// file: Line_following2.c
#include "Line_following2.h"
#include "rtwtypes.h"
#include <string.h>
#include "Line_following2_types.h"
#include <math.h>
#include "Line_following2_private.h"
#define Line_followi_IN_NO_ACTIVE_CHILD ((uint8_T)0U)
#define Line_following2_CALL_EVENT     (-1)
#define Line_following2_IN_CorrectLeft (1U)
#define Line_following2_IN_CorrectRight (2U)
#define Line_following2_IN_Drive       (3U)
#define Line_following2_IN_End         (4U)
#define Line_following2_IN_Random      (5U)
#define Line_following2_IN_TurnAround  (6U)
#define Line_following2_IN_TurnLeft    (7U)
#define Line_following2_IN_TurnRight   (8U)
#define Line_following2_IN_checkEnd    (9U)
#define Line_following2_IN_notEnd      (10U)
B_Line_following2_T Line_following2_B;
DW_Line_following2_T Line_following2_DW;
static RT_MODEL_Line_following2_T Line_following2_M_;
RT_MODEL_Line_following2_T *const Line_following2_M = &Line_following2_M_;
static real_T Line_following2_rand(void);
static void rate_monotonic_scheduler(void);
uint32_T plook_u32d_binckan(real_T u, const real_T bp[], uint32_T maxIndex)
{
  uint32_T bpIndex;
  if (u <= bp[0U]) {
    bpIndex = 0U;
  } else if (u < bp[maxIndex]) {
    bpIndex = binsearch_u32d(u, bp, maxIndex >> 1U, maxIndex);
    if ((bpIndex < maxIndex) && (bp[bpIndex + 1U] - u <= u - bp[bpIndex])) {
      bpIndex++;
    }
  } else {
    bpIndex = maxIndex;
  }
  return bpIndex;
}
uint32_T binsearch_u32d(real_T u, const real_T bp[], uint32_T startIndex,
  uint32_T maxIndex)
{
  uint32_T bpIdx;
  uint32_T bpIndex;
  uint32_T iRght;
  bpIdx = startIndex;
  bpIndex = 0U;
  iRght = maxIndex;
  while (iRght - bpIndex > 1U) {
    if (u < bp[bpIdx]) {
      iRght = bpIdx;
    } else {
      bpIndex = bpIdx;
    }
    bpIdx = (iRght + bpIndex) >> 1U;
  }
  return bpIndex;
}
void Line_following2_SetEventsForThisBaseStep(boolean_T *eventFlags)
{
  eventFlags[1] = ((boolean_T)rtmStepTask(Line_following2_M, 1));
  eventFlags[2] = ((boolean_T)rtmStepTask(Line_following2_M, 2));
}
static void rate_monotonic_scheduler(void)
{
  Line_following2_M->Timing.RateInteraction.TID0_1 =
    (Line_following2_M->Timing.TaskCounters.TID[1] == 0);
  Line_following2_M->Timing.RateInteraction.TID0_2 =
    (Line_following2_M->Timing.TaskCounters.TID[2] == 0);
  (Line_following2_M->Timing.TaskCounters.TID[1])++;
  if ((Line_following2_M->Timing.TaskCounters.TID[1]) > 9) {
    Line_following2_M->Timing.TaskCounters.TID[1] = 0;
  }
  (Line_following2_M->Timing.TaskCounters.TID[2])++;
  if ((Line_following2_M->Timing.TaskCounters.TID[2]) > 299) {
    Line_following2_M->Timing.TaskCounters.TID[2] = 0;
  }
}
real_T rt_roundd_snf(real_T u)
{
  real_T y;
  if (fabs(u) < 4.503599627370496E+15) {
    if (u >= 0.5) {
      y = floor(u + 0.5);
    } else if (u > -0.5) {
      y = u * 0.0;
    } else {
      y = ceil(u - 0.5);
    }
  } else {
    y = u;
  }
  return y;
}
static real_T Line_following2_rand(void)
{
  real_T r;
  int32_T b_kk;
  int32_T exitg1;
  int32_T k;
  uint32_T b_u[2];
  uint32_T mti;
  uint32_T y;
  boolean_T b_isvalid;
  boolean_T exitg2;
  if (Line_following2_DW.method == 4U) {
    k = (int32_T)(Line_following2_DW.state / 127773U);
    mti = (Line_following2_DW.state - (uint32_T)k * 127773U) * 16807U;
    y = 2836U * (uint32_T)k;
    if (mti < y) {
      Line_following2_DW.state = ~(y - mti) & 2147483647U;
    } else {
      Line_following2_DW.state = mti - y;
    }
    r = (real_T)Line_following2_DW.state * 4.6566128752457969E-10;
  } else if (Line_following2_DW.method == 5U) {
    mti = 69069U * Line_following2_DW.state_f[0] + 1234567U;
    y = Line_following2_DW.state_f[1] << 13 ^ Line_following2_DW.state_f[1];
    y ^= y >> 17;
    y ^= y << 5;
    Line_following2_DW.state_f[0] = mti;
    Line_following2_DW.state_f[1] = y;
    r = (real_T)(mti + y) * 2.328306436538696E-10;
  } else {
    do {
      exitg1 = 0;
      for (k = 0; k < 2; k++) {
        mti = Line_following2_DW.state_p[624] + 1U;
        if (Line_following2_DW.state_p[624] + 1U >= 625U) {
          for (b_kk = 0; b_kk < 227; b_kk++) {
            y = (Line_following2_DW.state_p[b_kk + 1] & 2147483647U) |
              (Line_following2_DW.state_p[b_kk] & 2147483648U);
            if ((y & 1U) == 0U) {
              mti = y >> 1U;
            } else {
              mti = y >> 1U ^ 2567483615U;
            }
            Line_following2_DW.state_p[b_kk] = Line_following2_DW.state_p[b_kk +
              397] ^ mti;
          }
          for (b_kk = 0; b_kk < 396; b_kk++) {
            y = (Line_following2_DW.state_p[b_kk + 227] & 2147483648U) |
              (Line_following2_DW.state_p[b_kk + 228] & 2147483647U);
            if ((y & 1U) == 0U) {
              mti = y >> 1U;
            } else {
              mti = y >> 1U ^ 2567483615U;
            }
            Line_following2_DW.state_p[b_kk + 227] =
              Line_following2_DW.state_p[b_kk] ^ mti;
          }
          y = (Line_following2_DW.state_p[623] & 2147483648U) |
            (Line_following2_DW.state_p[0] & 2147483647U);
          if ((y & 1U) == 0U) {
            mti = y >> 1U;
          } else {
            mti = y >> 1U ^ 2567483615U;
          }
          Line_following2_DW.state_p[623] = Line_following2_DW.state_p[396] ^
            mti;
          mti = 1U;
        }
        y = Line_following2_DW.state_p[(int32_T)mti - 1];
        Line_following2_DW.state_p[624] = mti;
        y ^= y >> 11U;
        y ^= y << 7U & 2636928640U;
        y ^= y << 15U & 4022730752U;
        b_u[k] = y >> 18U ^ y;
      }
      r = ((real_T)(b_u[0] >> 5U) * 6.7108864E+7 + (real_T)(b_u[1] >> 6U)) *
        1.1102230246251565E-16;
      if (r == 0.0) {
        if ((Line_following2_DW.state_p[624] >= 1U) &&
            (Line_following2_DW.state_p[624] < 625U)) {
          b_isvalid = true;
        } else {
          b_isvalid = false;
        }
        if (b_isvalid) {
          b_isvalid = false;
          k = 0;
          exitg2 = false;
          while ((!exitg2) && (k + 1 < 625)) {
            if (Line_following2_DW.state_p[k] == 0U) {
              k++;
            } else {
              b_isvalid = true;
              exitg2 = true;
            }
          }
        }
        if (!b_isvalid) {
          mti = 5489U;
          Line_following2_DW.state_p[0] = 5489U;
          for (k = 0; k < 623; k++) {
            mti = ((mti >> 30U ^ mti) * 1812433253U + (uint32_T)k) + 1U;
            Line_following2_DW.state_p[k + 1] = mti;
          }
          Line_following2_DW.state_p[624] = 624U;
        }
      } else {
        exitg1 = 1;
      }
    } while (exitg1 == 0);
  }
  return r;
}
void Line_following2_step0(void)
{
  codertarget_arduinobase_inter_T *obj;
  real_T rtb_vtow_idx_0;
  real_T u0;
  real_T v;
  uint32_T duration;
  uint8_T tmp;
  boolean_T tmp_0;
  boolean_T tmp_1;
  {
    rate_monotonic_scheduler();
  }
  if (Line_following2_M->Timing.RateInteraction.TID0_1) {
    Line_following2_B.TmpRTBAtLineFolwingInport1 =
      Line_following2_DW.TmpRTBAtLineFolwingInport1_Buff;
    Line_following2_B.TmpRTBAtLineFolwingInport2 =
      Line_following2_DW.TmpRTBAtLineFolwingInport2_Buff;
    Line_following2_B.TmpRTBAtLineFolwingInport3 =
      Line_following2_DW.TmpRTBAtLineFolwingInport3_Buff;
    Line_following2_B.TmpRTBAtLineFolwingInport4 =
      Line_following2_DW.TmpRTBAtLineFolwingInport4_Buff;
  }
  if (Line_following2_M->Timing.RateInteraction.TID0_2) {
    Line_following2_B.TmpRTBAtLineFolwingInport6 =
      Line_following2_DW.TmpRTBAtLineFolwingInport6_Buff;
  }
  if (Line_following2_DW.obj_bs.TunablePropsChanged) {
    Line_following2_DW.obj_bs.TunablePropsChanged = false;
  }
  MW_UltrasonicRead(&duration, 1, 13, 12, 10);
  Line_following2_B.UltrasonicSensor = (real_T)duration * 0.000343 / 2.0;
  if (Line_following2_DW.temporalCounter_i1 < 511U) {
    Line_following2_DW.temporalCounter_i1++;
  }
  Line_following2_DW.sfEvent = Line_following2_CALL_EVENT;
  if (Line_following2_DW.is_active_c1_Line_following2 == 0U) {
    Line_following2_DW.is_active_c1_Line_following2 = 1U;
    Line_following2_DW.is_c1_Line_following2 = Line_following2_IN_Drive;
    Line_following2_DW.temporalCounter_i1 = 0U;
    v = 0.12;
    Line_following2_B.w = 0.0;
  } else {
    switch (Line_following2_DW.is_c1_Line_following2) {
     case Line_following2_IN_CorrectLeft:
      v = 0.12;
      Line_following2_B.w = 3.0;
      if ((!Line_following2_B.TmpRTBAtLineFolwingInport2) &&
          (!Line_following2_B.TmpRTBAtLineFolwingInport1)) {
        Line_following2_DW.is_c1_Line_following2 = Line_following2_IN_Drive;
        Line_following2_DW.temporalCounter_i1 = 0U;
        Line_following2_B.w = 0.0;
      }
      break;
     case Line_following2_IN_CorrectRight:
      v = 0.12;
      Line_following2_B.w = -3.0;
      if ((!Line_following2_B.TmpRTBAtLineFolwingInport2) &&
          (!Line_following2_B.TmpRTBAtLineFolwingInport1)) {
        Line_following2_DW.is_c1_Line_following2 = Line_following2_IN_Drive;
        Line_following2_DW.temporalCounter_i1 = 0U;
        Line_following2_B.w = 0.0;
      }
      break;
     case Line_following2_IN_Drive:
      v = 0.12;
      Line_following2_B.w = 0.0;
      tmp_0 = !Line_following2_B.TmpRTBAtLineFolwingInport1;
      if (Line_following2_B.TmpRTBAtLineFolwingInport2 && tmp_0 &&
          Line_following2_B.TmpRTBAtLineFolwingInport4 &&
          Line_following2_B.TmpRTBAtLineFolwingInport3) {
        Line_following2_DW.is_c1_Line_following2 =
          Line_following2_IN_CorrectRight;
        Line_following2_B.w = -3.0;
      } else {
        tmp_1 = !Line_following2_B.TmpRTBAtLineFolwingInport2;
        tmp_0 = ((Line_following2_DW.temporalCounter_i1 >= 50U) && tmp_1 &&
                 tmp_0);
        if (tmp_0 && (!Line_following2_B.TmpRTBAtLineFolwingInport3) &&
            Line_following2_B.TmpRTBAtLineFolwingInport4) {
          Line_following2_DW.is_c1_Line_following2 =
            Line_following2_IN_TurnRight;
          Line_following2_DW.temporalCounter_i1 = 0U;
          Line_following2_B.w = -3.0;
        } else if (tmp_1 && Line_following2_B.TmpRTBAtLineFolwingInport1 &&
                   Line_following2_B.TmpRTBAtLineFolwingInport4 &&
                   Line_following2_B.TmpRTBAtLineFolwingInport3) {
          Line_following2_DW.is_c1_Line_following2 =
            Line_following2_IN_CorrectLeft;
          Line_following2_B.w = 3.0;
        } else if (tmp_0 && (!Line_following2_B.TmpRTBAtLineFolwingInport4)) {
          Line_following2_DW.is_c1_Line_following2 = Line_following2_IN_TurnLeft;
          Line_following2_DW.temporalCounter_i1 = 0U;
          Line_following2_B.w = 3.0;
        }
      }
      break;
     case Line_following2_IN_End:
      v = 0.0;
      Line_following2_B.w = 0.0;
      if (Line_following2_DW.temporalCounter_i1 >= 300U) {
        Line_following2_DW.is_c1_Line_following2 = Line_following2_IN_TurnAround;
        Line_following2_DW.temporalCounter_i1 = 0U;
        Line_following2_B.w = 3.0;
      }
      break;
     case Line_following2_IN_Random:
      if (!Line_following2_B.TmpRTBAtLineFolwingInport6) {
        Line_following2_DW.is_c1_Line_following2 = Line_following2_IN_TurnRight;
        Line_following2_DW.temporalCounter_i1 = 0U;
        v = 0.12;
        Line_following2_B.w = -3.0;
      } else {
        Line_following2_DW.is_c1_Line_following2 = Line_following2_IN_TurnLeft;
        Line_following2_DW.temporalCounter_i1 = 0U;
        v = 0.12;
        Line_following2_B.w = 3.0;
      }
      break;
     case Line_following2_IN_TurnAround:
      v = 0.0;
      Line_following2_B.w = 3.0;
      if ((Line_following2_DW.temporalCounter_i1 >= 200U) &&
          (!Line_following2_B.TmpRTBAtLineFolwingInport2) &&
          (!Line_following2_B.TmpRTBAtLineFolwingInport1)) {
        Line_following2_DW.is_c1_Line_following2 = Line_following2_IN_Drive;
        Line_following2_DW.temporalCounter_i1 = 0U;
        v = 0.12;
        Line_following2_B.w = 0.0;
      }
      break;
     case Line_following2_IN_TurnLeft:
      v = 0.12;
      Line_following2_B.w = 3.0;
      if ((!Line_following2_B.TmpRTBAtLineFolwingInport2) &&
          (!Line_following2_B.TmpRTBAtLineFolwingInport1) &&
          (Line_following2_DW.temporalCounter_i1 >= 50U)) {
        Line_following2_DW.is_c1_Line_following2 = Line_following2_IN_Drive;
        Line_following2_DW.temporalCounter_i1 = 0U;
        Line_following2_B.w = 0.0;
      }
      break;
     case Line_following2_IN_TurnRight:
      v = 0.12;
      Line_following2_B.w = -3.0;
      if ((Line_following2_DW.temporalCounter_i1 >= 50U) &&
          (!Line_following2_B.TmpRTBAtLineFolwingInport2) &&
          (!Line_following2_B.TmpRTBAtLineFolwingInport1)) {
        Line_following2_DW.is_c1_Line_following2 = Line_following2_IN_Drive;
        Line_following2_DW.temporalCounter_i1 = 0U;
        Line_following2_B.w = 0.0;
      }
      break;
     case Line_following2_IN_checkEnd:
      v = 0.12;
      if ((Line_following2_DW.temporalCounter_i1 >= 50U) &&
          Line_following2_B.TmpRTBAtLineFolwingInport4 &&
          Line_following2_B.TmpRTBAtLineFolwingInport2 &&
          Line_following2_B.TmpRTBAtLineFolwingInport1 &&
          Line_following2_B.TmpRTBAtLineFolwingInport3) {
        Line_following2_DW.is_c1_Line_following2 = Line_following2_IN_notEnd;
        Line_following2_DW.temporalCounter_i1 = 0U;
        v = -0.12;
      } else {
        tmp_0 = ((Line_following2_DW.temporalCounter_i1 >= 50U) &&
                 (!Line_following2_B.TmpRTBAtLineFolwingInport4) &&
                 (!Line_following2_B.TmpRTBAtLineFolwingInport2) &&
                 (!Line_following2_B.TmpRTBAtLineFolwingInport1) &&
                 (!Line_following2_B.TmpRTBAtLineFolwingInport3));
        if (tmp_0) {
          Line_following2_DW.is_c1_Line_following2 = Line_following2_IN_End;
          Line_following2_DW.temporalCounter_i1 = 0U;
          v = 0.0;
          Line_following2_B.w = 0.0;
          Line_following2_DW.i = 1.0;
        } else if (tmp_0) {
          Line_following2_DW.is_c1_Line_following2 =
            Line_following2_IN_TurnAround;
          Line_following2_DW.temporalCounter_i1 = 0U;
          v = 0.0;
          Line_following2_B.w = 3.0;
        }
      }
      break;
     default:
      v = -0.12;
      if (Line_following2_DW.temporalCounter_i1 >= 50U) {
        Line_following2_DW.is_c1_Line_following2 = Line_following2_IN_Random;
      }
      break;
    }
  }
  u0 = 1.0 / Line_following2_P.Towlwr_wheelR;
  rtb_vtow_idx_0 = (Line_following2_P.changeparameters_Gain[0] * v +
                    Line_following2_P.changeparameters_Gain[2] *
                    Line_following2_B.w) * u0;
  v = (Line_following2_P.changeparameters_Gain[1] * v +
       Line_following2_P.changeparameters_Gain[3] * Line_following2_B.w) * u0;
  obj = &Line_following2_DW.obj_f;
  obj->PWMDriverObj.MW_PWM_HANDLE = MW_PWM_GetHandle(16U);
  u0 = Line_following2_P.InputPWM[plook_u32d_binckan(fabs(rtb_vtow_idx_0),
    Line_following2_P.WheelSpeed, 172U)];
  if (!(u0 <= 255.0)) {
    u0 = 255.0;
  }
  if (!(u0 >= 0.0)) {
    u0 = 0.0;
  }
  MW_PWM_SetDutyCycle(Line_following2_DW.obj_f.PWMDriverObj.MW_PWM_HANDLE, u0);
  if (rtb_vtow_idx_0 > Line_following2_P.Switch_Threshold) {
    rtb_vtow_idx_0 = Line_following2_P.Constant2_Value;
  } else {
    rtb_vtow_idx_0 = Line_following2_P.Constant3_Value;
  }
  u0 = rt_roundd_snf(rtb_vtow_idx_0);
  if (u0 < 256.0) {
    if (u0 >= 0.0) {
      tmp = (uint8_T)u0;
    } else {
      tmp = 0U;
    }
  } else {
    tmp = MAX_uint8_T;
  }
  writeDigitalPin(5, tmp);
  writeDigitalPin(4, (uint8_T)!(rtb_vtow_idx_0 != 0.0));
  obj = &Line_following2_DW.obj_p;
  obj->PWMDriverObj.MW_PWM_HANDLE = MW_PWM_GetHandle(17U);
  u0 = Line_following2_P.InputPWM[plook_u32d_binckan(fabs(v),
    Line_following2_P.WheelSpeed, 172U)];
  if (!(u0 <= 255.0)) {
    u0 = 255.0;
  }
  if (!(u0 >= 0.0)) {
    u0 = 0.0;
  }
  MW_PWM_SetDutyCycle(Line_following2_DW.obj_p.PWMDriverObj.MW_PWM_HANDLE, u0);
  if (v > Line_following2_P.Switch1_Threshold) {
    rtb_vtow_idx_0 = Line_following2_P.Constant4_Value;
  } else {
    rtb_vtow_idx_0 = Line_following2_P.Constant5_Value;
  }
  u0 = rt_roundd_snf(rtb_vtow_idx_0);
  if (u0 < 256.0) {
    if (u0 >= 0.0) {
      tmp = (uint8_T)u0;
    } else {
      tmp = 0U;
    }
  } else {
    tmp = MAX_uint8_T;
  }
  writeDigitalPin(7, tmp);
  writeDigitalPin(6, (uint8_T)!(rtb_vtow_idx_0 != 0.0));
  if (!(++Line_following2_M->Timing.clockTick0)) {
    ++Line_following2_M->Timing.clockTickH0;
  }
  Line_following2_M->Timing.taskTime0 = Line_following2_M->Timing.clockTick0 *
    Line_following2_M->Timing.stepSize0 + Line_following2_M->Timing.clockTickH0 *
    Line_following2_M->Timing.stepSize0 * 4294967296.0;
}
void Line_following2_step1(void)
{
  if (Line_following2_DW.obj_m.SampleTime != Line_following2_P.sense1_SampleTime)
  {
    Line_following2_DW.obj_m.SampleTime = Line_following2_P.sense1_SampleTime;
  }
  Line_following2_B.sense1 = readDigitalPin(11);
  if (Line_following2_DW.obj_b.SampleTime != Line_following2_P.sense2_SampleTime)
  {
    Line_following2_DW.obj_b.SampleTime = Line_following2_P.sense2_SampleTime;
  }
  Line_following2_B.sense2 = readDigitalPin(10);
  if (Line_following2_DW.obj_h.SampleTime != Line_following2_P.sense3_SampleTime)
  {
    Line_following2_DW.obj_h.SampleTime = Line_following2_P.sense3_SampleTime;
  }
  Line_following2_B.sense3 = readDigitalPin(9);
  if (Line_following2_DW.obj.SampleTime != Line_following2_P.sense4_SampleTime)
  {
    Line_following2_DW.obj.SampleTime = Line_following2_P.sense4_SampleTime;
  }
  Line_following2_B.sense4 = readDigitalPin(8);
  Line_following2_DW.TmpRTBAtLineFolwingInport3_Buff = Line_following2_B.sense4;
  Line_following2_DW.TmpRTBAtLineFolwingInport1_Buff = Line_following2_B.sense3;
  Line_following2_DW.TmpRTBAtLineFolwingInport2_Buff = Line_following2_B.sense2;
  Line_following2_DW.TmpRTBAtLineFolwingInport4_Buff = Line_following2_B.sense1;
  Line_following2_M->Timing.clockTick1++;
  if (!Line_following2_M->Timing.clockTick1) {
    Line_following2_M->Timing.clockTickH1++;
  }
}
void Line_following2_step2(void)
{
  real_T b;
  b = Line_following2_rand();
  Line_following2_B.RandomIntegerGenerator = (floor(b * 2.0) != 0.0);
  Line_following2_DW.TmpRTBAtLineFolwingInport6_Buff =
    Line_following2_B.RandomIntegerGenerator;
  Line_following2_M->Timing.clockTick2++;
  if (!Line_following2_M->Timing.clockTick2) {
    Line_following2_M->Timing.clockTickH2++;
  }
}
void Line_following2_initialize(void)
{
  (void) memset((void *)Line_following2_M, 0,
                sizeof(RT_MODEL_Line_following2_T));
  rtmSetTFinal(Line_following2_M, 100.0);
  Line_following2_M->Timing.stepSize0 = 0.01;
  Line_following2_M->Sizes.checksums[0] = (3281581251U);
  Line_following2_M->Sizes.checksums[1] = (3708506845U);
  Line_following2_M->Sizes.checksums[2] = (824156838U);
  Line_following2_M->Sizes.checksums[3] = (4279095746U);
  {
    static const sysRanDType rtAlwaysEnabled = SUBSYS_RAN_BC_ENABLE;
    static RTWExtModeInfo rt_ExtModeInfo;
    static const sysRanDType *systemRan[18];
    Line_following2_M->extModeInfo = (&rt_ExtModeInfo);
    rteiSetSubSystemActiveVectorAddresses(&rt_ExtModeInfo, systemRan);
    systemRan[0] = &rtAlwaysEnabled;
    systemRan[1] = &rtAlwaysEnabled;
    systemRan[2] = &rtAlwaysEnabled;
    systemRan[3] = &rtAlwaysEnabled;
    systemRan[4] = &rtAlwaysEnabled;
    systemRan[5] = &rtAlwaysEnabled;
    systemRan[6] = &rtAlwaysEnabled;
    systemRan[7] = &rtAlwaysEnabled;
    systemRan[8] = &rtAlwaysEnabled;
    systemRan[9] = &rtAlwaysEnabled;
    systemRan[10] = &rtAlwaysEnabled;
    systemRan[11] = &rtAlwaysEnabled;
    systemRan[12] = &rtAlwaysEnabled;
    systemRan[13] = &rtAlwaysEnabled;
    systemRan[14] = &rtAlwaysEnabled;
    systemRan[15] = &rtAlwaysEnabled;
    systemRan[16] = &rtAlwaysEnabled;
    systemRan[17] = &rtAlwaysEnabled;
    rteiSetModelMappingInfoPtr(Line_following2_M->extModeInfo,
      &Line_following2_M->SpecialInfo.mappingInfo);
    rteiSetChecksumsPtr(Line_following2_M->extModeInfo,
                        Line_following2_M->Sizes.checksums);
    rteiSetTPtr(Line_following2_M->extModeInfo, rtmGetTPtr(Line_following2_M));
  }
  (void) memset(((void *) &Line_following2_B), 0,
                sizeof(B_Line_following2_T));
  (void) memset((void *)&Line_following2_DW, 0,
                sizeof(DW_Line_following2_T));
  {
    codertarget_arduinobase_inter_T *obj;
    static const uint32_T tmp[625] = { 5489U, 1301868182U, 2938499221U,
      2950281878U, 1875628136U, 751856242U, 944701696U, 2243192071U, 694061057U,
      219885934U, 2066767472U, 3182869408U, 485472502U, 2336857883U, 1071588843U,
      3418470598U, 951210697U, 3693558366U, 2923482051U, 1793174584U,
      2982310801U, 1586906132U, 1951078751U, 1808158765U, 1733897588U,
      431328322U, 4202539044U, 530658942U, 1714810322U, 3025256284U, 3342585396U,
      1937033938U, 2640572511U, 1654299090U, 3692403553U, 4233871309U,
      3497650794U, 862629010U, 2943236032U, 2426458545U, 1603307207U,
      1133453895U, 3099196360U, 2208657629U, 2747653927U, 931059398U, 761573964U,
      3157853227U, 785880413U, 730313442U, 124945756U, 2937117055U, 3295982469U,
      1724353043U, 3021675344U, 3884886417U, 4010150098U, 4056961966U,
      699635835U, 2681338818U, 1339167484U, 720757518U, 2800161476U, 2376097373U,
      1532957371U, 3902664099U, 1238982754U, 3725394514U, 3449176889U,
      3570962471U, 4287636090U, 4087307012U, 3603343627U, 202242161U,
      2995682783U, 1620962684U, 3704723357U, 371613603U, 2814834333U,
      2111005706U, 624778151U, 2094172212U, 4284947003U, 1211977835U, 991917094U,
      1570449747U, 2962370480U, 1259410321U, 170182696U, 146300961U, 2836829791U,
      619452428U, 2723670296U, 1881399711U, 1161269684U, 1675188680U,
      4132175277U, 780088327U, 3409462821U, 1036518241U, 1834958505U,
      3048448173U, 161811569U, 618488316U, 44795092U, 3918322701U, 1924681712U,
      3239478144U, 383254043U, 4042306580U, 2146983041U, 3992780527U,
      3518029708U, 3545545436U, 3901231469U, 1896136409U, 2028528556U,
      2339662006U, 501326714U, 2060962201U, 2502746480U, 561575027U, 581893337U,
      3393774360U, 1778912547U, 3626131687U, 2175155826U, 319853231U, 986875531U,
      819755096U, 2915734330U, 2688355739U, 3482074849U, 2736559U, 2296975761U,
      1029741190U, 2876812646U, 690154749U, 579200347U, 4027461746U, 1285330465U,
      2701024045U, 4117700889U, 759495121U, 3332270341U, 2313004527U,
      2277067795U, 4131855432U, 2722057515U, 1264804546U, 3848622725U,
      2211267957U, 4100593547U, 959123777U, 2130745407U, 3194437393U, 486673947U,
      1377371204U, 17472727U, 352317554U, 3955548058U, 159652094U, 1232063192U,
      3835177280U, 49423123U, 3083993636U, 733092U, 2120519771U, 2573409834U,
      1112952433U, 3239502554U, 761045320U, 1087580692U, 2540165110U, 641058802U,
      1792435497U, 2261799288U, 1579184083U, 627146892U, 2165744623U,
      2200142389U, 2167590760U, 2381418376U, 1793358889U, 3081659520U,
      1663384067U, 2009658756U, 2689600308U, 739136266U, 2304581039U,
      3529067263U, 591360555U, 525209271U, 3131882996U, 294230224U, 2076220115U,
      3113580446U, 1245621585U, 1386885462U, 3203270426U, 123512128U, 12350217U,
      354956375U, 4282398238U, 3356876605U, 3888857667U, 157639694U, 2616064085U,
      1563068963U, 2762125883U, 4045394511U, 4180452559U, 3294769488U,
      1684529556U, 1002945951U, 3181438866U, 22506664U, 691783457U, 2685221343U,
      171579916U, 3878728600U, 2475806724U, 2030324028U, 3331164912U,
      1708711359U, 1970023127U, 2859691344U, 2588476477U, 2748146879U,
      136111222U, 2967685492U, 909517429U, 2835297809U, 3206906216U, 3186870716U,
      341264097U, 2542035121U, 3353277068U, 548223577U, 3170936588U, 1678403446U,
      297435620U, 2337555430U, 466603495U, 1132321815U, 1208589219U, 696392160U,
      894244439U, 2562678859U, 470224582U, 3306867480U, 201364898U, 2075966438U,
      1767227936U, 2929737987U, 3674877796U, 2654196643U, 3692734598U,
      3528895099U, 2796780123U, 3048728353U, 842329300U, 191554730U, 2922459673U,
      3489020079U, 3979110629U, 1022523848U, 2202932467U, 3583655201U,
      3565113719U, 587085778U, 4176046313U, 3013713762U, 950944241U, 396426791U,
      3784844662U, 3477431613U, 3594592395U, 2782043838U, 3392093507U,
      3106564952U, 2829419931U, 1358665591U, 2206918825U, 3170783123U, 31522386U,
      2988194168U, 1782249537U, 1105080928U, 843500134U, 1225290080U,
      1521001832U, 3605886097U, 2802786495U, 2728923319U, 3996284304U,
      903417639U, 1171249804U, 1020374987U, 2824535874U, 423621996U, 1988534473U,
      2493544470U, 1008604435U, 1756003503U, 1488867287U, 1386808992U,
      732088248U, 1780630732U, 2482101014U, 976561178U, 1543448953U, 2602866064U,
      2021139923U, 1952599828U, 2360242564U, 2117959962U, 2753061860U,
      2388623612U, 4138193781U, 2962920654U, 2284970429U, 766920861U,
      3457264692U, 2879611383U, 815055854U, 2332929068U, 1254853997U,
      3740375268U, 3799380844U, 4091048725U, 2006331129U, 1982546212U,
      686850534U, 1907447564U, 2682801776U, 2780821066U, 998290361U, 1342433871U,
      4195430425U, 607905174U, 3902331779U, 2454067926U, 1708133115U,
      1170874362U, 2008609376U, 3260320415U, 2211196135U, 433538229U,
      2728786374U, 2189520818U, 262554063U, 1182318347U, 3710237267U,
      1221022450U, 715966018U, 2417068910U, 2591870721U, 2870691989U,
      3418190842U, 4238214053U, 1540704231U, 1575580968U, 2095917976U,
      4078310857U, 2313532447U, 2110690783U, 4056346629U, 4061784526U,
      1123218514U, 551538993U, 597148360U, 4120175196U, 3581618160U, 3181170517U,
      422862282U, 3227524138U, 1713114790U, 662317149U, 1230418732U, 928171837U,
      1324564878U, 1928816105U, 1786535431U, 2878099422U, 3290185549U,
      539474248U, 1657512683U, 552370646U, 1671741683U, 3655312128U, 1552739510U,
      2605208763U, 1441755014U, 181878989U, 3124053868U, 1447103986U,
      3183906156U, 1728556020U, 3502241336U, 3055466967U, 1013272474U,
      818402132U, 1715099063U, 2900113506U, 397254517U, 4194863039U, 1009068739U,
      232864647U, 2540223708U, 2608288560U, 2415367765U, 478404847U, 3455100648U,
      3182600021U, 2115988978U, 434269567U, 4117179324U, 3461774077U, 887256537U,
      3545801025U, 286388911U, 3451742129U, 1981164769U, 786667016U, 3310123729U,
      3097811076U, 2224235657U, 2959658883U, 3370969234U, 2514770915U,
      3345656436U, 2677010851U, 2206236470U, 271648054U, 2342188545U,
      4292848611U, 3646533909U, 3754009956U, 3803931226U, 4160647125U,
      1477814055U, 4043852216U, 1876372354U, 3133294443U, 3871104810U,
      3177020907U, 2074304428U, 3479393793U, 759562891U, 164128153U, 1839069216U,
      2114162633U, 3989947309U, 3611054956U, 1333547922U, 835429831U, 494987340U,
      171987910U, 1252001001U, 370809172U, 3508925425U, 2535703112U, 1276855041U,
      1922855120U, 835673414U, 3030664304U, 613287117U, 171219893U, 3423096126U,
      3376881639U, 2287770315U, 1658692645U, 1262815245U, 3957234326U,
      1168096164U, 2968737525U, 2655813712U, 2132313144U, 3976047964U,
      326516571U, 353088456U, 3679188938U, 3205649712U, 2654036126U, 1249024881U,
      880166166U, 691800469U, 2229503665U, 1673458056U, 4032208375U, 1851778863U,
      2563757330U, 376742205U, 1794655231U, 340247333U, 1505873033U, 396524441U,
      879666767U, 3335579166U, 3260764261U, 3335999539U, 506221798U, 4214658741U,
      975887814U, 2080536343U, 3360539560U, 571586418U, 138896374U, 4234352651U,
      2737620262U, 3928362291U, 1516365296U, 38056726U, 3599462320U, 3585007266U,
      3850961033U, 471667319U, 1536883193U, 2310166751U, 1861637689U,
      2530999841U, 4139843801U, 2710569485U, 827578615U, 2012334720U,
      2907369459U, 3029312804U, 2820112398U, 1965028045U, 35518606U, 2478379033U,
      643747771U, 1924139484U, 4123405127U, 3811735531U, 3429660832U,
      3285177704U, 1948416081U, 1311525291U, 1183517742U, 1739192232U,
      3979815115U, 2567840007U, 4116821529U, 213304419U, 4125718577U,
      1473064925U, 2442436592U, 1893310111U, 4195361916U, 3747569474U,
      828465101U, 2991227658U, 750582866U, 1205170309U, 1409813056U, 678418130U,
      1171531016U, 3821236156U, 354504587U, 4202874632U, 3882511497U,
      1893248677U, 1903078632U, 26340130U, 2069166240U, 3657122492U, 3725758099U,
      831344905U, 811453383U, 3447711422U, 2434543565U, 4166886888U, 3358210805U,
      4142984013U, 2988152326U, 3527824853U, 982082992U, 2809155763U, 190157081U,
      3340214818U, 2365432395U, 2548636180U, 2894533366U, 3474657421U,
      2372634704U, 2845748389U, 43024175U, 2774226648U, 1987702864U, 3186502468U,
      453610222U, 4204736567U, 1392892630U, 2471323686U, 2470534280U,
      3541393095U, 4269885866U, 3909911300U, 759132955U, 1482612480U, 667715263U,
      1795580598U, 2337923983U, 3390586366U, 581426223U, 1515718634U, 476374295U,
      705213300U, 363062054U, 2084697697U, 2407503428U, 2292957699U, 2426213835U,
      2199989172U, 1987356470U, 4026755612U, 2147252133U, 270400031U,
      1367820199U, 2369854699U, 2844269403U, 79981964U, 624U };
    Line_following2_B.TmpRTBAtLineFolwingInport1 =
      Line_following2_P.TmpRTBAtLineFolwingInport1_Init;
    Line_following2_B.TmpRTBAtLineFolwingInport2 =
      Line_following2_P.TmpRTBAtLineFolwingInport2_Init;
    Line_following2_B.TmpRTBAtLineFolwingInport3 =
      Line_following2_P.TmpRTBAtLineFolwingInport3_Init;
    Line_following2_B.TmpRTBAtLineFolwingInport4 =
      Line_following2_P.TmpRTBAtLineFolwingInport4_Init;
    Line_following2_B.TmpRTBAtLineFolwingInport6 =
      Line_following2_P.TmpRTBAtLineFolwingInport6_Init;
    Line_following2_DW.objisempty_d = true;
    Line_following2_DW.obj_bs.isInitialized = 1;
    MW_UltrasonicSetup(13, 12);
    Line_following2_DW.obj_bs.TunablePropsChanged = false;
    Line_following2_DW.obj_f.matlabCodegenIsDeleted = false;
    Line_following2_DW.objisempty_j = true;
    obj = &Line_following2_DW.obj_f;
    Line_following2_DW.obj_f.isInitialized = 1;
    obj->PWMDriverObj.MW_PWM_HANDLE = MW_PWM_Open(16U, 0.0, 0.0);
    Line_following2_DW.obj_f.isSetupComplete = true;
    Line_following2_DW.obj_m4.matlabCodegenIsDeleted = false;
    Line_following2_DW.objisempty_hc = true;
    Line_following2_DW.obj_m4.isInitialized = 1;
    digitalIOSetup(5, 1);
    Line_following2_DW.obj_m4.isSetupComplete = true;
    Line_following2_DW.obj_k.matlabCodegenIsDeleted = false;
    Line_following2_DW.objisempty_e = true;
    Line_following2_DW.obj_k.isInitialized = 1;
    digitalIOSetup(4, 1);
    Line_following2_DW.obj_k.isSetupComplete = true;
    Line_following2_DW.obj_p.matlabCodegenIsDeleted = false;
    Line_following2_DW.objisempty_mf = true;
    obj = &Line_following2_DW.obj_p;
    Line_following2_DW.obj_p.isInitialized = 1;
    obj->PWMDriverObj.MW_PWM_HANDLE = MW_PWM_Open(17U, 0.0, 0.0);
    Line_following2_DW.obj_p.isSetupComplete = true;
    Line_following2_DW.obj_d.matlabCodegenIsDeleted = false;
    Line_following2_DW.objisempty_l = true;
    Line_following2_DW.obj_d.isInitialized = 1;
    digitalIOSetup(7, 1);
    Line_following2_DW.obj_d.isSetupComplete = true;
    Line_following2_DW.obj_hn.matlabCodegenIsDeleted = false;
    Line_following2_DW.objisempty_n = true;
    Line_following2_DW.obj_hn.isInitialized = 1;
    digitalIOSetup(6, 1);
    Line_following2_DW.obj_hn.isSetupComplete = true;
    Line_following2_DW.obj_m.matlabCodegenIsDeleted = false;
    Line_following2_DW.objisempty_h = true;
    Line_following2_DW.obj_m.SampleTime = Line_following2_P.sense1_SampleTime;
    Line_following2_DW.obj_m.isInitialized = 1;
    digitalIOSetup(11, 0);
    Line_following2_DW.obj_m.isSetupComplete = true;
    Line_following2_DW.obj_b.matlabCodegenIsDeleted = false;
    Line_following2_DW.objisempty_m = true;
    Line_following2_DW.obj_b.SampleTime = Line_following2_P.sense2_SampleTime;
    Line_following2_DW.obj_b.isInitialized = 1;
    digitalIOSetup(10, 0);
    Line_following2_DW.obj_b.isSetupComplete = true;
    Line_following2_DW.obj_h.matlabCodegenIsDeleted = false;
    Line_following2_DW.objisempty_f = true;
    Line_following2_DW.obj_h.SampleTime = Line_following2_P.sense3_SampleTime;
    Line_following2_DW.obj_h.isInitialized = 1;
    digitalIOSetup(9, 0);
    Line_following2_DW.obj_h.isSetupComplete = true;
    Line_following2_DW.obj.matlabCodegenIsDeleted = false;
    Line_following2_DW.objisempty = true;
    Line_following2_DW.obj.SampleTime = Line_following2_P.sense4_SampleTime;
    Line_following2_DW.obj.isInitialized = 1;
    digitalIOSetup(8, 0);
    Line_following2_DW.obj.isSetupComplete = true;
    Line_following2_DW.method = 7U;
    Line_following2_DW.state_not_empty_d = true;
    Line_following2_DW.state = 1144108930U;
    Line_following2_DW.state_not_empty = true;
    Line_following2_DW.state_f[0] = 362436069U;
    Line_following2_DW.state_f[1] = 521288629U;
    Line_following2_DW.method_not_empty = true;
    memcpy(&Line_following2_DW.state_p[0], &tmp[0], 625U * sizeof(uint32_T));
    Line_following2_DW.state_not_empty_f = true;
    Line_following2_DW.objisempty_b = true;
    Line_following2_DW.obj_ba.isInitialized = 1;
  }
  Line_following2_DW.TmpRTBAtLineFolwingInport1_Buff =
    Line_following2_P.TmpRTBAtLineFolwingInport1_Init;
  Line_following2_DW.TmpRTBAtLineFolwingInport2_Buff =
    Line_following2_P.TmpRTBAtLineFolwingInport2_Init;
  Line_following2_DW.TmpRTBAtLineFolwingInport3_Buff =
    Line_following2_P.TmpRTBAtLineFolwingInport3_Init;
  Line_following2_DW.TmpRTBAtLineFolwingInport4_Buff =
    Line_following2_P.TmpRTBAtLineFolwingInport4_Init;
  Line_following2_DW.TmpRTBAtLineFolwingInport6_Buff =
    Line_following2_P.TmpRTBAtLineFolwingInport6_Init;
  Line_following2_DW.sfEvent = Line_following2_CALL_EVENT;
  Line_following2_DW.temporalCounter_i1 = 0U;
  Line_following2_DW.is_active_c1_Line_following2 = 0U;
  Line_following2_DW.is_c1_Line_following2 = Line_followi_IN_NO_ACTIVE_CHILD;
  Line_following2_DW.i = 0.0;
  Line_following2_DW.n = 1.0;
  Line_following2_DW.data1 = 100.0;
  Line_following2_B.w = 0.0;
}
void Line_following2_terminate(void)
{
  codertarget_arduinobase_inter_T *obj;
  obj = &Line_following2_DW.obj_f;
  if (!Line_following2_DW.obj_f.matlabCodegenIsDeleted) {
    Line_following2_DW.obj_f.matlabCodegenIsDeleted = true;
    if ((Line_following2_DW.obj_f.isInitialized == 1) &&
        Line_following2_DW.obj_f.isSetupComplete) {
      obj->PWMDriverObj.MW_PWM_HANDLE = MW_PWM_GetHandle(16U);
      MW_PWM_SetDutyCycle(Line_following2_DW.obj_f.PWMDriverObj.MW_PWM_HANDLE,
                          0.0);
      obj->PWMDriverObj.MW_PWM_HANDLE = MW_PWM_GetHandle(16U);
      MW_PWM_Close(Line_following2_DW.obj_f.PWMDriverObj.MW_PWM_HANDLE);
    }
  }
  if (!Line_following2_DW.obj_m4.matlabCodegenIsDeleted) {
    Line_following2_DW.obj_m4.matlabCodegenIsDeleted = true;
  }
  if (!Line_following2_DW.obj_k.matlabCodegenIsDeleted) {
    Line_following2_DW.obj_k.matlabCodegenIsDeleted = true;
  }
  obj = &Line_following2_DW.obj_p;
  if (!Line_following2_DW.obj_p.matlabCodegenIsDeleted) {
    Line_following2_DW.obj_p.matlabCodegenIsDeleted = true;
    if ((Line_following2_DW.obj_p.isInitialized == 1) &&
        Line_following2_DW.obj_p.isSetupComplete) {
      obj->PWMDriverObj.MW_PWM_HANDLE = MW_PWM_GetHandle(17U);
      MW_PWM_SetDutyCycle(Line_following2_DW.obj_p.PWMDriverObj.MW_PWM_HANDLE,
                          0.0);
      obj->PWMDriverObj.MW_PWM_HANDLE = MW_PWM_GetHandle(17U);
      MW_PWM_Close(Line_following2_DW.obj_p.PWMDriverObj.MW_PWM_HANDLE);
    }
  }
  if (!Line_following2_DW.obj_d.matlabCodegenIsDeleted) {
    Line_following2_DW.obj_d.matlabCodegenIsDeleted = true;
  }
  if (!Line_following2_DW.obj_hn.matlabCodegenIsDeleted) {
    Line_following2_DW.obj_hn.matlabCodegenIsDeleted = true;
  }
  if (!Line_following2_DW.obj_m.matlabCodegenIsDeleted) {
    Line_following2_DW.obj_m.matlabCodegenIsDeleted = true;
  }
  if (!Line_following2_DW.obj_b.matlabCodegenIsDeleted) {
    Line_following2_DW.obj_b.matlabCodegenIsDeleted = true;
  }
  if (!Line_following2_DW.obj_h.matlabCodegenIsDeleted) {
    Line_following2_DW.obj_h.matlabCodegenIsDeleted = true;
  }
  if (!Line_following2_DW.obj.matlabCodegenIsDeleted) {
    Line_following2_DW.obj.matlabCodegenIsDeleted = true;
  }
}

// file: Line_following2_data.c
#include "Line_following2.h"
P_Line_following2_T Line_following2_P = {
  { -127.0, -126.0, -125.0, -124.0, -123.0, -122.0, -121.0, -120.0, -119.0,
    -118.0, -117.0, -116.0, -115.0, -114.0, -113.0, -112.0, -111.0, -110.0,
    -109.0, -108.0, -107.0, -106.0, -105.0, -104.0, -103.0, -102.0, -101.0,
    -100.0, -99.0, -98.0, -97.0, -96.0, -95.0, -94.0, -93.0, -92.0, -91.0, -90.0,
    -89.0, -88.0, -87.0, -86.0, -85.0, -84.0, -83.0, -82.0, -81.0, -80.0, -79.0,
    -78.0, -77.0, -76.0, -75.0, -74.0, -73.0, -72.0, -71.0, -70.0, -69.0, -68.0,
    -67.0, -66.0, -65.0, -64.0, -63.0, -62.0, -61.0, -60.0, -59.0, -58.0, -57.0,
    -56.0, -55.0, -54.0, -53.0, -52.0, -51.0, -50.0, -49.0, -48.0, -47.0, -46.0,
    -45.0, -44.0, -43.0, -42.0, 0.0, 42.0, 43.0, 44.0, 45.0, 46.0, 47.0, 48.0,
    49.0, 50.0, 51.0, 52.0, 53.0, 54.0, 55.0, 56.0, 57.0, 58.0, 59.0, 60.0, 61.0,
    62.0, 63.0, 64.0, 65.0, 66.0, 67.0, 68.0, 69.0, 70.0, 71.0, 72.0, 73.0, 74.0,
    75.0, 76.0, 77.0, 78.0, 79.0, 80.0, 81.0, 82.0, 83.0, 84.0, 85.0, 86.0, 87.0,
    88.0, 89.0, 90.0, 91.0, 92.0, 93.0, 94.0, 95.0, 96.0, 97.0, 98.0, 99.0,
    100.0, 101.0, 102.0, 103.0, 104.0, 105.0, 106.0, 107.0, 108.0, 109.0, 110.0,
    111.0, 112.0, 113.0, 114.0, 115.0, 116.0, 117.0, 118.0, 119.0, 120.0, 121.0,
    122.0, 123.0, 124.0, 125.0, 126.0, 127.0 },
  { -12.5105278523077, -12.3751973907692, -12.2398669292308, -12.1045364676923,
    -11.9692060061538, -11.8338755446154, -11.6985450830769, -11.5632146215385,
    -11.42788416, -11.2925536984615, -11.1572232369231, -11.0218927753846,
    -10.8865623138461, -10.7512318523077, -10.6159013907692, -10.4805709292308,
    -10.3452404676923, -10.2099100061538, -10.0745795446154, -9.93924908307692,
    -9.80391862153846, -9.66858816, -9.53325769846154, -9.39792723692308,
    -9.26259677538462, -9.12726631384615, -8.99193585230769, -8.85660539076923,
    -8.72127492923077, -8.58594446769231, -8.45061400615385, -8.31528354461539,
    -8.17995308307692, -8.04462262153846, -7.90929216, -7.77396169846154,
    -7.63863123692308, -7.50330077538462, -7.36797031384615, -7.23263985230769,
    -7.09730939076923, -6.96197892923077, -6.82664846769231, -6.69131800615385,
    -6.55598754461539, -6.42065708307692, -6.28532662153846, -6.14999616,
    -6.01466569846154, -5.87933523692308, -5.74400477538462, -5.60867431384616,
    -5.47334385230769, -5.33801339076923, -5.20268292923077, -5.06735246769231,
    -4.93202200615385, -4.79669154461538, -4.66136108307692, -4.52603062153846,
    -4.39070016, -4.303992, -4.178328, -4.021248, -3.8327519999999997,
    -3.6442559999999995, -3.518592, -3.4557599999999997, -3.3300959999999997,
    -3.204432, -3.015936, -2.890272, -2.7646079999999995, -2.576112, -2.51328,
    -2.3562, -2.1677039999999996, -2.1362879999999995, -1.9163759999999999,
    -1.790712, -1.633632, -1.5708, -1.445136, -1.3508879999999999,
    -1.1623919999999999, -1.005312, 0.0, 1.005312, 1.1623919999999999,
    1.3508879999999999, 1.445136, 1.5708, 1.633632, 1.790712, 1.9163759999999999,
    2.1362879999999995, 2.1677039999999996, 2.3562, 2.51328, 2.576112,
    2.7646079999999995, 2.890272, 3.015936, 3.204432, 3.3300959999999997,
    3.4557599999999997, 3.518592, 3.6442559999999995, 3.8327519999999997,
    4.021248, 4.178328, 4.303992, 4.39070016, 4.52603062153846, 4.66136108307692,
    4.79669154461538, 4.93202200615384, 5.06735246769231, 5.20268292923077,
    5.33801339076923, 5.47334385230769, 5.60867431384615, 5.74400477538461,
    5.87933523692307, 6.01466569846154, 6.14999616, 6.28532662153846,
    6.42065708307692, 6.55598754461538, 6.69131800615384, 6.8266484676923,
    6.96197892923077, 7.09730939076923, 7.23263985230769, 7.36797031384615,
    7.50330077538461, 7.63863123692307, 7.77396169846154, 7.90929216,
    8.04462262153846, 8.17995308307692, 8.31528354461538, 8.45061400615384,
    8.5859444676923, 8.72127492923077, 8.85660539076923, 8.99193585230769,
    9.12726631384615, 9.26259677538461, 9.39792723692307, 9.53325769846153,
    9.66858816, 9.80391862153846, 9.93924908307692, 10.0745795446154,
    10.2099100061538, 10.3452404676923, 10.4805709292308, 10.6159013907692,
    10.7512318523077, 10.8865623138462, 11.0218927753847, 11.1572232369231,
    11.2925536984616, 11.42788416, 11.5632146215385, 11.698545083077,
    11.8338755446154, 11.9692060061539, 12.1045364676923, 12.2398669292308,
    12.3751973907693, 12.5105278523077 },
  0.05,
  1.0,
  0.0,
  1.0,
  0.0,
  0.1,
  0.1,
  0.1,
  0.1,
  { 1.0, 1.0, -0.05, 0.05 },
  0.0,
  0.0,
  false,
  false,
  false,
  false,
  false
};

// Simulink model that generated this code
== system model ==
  PWM#1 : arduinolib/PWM  pinNumber=16  <- 1: Lookup_nD#1
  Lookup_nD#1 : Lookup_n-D  BreakpointsForDimension1=WheelSpeed  Table=InputPWM  InterpMethod=Nearest  <- 1: Abs#1
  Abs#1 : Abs  <- 1: Towlwr
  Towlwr : mobileRoboticsTrainingLib/To wlwr  <- 1: Stateflowchart#1, 2: Stateflowchart#1/2
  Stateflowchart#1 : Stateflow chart  <- 1: sense3, 2: sense2, 3: sense4, 4: sense1, 5: UltrasonicSensor, 6: RandomIntegerGenerator
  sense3 : arduinolib/Digital Input  pinNumber=9
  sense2 : arduinolib/Digital Input  pinNumber=10
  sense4 : arduinolib/Digital Input  pinNumber=8
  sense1 : arduinolib/Digital Input  pinNumber=11
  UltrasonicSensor : arduinosensorlib/Ultrasonic Sensor
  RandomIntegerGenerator : commrandsrc3/Random Integer Generator
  DigitalOutput#1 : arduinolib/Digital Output  pinNumber=5  <- 1: Switch
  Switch : Switch  Criteria=u2 > Threshold  <- 1: Constant2, 2: Towlwr, 3: Constant3
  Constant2 : Constant
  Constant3 : Constant  Value=0
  DigitalOutput#2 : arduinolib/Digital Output  pinNumber=4  <- 1: Logic#1
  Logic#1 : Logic  Operator=NOT  <- 1: Switch
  PWM#2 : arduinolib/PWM  pinNumber=17  <- 1: Lookup_nD#2
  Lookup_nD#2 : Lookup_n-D  BreakpointsForDimension1=WheelSpeed  Table=InputPWM  InterpMethod=Nearest  <- 1: Abs#2
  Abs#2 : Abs  <- 1: Towlwr/2
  DigitalOutput#3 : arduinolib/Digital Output  pinNumber=7  <- 1: Switch1
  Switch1 : Switch  Criteria=u2 > Threshold  <- 1: Constant4, 2: Towlwr/2, 3: Constant5
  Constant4 : Constant
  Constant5 : Constant  Value=0
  DigitalOutput#4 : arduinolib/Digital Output  pinNumber=6  <- 1: Logic#2
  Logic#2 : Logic  Operator=NOT  <- 1: Switch1
== stateflow chart Stateflowchart#1 ==
  state Random
    entry:
    dir;
  state notEnd
    entry:
    v=-0.12;
  state End
    entry:
    v=0;
    w=0;
    i=1;
  state TurnAround
    entry:
    v=0;
    w=3;
  state checkEnd
    entry:
    v=0.12;
  state TurnLeft
    entry:
    v=0.12;
    w=3;
  state TurnRight
    entry:
    v=0.12;
    w=-3;
  state Drive
    entry:
    v=0.12;
    w=0;
    i;
    n;
    data1;
  state CorrectLeft
    entry:
    v=0.12;
    w=3
  state CorrectRight
    entry:
    v=0.12;
    w=-3
  state ObjectDetected
    entry:
    v=0.12;
  state CorrectRight1
    entry:
    w=-3;
  state CorrectLeft1
    entry:
    w=3;
  state TurnAround1
    entry:
    w=3;
  state EndOfLine
    entry:
    v=0;
  state update
    entry:
    data1=ultraSonic;
  state WeOUT
    entry:
    v=0;
    w=0;
  checkEnd -> TurnAround [order 3] : [after(0.5,sec) &&sense1 ==0 && sense2 == 0 && sense3 ==0 && sense4==0 && i==1]
  Random -> TurnLeft [order 2] : [dir==1]
  Random -> TurnRight [order 1] : [dir==0]
  notEnd -> Random : [after(0.5,sec)]
  checkEnd -> notEnd [order 1] : [after(0.5,sec) &&sense1 == 1 && sense2 == 1 && sense3 ==1 && sense4==1 ]
  End -> TurnAround : [after(3,sec)]
  checkEnd -> End [order 2] : [after(0.5,sec) &&sense1 ==0 && sense2 == 0 && sense3 ==0 && sense4==0 && i==0]
  TurnAround -> Drive : [after(2,sec) && sense2 == 0 && sense3 == 0]
  Drive -> checkEnd [order 2] : [sense1 == 0 && sense2 == 0 && sense3 == 0 && sense4==0]
  (default) -> Drive
  TurnRight -> Drive : [after(0.5,sec) && sense2 ==0 && sense3 ==0]
  Drive -> TurnLeft [order 6] : [after(0.5,sec) && sense2 == 0 && sense3 == 0 && sense1 == 0 ]
  TurnLeft -> Drive : [sense2==0 && sense3==0 && after(0.5,sec)]
  Drive -> TurnRight [order 3] : [after(0.5,sec) && sense2 == 0 && sense3 == 0 && sense4 == 0 && sense1==1]
  Drive -> CorrectLeft [order 4] : [sense2==0 && sense3 ==1 && sense1 == 1 &&sense4 ==1]
  Drive -> CorrectRight [order 1] : [sense2==1 && sense3 ==0 && sense1 == 1 &&sense4 ==1]
  CorrectLeft -> Drive : [sense2 ==0 && sense3 ==0]
  CorrectRight -> Drive : [sense2==0 && sense3 == 0]
  TurnAround1 -> Drive : [after(1,sec) && sense2 == 0 && sense3 == 0]
  Drive -> EndOfLine [order 7] : [sense1 == 1 && sense2 == 1 && sense3 == 1 && sense4==1]
  Drive -> ObjectDetected [order 5] : [ultraSonic ~= 0]
  ObjectDetected -> CorrectRight1 [order 2] : [sense2==1 && sense3 ==0]
  ObjectDetected -> CorrectLeft1 [order 3] : [sense2==0 && sense3 ==1]
  CorrectRight1 -> ObjectDetected : [sense2==0 && sense3 == 0]
  CorrectLeft1 -> ObjectDetected : [sense2 ==0 && sense3 ==0]
  ObjectDetected -> EndOfLine [order 1] : [sense1 == 0 && sense4 == 0]
  EndOfLine -> TurnAround1 [order 2] : [after(1,sec)]
  update -> EndOfLine
  EndOfLine -> update [order 1] : [ultraSonic<data1 && ultraSonic~=0 && i==0]
  EndOfLine -> WeOUT [order 3] : [i==1 && ultraSonic==data1]
  data: v output; w output; sense3 input; sense2 input; sense4 input; sense1 input; ultraSonic input; i local =0; dir input; n local =1; data1 local =100
